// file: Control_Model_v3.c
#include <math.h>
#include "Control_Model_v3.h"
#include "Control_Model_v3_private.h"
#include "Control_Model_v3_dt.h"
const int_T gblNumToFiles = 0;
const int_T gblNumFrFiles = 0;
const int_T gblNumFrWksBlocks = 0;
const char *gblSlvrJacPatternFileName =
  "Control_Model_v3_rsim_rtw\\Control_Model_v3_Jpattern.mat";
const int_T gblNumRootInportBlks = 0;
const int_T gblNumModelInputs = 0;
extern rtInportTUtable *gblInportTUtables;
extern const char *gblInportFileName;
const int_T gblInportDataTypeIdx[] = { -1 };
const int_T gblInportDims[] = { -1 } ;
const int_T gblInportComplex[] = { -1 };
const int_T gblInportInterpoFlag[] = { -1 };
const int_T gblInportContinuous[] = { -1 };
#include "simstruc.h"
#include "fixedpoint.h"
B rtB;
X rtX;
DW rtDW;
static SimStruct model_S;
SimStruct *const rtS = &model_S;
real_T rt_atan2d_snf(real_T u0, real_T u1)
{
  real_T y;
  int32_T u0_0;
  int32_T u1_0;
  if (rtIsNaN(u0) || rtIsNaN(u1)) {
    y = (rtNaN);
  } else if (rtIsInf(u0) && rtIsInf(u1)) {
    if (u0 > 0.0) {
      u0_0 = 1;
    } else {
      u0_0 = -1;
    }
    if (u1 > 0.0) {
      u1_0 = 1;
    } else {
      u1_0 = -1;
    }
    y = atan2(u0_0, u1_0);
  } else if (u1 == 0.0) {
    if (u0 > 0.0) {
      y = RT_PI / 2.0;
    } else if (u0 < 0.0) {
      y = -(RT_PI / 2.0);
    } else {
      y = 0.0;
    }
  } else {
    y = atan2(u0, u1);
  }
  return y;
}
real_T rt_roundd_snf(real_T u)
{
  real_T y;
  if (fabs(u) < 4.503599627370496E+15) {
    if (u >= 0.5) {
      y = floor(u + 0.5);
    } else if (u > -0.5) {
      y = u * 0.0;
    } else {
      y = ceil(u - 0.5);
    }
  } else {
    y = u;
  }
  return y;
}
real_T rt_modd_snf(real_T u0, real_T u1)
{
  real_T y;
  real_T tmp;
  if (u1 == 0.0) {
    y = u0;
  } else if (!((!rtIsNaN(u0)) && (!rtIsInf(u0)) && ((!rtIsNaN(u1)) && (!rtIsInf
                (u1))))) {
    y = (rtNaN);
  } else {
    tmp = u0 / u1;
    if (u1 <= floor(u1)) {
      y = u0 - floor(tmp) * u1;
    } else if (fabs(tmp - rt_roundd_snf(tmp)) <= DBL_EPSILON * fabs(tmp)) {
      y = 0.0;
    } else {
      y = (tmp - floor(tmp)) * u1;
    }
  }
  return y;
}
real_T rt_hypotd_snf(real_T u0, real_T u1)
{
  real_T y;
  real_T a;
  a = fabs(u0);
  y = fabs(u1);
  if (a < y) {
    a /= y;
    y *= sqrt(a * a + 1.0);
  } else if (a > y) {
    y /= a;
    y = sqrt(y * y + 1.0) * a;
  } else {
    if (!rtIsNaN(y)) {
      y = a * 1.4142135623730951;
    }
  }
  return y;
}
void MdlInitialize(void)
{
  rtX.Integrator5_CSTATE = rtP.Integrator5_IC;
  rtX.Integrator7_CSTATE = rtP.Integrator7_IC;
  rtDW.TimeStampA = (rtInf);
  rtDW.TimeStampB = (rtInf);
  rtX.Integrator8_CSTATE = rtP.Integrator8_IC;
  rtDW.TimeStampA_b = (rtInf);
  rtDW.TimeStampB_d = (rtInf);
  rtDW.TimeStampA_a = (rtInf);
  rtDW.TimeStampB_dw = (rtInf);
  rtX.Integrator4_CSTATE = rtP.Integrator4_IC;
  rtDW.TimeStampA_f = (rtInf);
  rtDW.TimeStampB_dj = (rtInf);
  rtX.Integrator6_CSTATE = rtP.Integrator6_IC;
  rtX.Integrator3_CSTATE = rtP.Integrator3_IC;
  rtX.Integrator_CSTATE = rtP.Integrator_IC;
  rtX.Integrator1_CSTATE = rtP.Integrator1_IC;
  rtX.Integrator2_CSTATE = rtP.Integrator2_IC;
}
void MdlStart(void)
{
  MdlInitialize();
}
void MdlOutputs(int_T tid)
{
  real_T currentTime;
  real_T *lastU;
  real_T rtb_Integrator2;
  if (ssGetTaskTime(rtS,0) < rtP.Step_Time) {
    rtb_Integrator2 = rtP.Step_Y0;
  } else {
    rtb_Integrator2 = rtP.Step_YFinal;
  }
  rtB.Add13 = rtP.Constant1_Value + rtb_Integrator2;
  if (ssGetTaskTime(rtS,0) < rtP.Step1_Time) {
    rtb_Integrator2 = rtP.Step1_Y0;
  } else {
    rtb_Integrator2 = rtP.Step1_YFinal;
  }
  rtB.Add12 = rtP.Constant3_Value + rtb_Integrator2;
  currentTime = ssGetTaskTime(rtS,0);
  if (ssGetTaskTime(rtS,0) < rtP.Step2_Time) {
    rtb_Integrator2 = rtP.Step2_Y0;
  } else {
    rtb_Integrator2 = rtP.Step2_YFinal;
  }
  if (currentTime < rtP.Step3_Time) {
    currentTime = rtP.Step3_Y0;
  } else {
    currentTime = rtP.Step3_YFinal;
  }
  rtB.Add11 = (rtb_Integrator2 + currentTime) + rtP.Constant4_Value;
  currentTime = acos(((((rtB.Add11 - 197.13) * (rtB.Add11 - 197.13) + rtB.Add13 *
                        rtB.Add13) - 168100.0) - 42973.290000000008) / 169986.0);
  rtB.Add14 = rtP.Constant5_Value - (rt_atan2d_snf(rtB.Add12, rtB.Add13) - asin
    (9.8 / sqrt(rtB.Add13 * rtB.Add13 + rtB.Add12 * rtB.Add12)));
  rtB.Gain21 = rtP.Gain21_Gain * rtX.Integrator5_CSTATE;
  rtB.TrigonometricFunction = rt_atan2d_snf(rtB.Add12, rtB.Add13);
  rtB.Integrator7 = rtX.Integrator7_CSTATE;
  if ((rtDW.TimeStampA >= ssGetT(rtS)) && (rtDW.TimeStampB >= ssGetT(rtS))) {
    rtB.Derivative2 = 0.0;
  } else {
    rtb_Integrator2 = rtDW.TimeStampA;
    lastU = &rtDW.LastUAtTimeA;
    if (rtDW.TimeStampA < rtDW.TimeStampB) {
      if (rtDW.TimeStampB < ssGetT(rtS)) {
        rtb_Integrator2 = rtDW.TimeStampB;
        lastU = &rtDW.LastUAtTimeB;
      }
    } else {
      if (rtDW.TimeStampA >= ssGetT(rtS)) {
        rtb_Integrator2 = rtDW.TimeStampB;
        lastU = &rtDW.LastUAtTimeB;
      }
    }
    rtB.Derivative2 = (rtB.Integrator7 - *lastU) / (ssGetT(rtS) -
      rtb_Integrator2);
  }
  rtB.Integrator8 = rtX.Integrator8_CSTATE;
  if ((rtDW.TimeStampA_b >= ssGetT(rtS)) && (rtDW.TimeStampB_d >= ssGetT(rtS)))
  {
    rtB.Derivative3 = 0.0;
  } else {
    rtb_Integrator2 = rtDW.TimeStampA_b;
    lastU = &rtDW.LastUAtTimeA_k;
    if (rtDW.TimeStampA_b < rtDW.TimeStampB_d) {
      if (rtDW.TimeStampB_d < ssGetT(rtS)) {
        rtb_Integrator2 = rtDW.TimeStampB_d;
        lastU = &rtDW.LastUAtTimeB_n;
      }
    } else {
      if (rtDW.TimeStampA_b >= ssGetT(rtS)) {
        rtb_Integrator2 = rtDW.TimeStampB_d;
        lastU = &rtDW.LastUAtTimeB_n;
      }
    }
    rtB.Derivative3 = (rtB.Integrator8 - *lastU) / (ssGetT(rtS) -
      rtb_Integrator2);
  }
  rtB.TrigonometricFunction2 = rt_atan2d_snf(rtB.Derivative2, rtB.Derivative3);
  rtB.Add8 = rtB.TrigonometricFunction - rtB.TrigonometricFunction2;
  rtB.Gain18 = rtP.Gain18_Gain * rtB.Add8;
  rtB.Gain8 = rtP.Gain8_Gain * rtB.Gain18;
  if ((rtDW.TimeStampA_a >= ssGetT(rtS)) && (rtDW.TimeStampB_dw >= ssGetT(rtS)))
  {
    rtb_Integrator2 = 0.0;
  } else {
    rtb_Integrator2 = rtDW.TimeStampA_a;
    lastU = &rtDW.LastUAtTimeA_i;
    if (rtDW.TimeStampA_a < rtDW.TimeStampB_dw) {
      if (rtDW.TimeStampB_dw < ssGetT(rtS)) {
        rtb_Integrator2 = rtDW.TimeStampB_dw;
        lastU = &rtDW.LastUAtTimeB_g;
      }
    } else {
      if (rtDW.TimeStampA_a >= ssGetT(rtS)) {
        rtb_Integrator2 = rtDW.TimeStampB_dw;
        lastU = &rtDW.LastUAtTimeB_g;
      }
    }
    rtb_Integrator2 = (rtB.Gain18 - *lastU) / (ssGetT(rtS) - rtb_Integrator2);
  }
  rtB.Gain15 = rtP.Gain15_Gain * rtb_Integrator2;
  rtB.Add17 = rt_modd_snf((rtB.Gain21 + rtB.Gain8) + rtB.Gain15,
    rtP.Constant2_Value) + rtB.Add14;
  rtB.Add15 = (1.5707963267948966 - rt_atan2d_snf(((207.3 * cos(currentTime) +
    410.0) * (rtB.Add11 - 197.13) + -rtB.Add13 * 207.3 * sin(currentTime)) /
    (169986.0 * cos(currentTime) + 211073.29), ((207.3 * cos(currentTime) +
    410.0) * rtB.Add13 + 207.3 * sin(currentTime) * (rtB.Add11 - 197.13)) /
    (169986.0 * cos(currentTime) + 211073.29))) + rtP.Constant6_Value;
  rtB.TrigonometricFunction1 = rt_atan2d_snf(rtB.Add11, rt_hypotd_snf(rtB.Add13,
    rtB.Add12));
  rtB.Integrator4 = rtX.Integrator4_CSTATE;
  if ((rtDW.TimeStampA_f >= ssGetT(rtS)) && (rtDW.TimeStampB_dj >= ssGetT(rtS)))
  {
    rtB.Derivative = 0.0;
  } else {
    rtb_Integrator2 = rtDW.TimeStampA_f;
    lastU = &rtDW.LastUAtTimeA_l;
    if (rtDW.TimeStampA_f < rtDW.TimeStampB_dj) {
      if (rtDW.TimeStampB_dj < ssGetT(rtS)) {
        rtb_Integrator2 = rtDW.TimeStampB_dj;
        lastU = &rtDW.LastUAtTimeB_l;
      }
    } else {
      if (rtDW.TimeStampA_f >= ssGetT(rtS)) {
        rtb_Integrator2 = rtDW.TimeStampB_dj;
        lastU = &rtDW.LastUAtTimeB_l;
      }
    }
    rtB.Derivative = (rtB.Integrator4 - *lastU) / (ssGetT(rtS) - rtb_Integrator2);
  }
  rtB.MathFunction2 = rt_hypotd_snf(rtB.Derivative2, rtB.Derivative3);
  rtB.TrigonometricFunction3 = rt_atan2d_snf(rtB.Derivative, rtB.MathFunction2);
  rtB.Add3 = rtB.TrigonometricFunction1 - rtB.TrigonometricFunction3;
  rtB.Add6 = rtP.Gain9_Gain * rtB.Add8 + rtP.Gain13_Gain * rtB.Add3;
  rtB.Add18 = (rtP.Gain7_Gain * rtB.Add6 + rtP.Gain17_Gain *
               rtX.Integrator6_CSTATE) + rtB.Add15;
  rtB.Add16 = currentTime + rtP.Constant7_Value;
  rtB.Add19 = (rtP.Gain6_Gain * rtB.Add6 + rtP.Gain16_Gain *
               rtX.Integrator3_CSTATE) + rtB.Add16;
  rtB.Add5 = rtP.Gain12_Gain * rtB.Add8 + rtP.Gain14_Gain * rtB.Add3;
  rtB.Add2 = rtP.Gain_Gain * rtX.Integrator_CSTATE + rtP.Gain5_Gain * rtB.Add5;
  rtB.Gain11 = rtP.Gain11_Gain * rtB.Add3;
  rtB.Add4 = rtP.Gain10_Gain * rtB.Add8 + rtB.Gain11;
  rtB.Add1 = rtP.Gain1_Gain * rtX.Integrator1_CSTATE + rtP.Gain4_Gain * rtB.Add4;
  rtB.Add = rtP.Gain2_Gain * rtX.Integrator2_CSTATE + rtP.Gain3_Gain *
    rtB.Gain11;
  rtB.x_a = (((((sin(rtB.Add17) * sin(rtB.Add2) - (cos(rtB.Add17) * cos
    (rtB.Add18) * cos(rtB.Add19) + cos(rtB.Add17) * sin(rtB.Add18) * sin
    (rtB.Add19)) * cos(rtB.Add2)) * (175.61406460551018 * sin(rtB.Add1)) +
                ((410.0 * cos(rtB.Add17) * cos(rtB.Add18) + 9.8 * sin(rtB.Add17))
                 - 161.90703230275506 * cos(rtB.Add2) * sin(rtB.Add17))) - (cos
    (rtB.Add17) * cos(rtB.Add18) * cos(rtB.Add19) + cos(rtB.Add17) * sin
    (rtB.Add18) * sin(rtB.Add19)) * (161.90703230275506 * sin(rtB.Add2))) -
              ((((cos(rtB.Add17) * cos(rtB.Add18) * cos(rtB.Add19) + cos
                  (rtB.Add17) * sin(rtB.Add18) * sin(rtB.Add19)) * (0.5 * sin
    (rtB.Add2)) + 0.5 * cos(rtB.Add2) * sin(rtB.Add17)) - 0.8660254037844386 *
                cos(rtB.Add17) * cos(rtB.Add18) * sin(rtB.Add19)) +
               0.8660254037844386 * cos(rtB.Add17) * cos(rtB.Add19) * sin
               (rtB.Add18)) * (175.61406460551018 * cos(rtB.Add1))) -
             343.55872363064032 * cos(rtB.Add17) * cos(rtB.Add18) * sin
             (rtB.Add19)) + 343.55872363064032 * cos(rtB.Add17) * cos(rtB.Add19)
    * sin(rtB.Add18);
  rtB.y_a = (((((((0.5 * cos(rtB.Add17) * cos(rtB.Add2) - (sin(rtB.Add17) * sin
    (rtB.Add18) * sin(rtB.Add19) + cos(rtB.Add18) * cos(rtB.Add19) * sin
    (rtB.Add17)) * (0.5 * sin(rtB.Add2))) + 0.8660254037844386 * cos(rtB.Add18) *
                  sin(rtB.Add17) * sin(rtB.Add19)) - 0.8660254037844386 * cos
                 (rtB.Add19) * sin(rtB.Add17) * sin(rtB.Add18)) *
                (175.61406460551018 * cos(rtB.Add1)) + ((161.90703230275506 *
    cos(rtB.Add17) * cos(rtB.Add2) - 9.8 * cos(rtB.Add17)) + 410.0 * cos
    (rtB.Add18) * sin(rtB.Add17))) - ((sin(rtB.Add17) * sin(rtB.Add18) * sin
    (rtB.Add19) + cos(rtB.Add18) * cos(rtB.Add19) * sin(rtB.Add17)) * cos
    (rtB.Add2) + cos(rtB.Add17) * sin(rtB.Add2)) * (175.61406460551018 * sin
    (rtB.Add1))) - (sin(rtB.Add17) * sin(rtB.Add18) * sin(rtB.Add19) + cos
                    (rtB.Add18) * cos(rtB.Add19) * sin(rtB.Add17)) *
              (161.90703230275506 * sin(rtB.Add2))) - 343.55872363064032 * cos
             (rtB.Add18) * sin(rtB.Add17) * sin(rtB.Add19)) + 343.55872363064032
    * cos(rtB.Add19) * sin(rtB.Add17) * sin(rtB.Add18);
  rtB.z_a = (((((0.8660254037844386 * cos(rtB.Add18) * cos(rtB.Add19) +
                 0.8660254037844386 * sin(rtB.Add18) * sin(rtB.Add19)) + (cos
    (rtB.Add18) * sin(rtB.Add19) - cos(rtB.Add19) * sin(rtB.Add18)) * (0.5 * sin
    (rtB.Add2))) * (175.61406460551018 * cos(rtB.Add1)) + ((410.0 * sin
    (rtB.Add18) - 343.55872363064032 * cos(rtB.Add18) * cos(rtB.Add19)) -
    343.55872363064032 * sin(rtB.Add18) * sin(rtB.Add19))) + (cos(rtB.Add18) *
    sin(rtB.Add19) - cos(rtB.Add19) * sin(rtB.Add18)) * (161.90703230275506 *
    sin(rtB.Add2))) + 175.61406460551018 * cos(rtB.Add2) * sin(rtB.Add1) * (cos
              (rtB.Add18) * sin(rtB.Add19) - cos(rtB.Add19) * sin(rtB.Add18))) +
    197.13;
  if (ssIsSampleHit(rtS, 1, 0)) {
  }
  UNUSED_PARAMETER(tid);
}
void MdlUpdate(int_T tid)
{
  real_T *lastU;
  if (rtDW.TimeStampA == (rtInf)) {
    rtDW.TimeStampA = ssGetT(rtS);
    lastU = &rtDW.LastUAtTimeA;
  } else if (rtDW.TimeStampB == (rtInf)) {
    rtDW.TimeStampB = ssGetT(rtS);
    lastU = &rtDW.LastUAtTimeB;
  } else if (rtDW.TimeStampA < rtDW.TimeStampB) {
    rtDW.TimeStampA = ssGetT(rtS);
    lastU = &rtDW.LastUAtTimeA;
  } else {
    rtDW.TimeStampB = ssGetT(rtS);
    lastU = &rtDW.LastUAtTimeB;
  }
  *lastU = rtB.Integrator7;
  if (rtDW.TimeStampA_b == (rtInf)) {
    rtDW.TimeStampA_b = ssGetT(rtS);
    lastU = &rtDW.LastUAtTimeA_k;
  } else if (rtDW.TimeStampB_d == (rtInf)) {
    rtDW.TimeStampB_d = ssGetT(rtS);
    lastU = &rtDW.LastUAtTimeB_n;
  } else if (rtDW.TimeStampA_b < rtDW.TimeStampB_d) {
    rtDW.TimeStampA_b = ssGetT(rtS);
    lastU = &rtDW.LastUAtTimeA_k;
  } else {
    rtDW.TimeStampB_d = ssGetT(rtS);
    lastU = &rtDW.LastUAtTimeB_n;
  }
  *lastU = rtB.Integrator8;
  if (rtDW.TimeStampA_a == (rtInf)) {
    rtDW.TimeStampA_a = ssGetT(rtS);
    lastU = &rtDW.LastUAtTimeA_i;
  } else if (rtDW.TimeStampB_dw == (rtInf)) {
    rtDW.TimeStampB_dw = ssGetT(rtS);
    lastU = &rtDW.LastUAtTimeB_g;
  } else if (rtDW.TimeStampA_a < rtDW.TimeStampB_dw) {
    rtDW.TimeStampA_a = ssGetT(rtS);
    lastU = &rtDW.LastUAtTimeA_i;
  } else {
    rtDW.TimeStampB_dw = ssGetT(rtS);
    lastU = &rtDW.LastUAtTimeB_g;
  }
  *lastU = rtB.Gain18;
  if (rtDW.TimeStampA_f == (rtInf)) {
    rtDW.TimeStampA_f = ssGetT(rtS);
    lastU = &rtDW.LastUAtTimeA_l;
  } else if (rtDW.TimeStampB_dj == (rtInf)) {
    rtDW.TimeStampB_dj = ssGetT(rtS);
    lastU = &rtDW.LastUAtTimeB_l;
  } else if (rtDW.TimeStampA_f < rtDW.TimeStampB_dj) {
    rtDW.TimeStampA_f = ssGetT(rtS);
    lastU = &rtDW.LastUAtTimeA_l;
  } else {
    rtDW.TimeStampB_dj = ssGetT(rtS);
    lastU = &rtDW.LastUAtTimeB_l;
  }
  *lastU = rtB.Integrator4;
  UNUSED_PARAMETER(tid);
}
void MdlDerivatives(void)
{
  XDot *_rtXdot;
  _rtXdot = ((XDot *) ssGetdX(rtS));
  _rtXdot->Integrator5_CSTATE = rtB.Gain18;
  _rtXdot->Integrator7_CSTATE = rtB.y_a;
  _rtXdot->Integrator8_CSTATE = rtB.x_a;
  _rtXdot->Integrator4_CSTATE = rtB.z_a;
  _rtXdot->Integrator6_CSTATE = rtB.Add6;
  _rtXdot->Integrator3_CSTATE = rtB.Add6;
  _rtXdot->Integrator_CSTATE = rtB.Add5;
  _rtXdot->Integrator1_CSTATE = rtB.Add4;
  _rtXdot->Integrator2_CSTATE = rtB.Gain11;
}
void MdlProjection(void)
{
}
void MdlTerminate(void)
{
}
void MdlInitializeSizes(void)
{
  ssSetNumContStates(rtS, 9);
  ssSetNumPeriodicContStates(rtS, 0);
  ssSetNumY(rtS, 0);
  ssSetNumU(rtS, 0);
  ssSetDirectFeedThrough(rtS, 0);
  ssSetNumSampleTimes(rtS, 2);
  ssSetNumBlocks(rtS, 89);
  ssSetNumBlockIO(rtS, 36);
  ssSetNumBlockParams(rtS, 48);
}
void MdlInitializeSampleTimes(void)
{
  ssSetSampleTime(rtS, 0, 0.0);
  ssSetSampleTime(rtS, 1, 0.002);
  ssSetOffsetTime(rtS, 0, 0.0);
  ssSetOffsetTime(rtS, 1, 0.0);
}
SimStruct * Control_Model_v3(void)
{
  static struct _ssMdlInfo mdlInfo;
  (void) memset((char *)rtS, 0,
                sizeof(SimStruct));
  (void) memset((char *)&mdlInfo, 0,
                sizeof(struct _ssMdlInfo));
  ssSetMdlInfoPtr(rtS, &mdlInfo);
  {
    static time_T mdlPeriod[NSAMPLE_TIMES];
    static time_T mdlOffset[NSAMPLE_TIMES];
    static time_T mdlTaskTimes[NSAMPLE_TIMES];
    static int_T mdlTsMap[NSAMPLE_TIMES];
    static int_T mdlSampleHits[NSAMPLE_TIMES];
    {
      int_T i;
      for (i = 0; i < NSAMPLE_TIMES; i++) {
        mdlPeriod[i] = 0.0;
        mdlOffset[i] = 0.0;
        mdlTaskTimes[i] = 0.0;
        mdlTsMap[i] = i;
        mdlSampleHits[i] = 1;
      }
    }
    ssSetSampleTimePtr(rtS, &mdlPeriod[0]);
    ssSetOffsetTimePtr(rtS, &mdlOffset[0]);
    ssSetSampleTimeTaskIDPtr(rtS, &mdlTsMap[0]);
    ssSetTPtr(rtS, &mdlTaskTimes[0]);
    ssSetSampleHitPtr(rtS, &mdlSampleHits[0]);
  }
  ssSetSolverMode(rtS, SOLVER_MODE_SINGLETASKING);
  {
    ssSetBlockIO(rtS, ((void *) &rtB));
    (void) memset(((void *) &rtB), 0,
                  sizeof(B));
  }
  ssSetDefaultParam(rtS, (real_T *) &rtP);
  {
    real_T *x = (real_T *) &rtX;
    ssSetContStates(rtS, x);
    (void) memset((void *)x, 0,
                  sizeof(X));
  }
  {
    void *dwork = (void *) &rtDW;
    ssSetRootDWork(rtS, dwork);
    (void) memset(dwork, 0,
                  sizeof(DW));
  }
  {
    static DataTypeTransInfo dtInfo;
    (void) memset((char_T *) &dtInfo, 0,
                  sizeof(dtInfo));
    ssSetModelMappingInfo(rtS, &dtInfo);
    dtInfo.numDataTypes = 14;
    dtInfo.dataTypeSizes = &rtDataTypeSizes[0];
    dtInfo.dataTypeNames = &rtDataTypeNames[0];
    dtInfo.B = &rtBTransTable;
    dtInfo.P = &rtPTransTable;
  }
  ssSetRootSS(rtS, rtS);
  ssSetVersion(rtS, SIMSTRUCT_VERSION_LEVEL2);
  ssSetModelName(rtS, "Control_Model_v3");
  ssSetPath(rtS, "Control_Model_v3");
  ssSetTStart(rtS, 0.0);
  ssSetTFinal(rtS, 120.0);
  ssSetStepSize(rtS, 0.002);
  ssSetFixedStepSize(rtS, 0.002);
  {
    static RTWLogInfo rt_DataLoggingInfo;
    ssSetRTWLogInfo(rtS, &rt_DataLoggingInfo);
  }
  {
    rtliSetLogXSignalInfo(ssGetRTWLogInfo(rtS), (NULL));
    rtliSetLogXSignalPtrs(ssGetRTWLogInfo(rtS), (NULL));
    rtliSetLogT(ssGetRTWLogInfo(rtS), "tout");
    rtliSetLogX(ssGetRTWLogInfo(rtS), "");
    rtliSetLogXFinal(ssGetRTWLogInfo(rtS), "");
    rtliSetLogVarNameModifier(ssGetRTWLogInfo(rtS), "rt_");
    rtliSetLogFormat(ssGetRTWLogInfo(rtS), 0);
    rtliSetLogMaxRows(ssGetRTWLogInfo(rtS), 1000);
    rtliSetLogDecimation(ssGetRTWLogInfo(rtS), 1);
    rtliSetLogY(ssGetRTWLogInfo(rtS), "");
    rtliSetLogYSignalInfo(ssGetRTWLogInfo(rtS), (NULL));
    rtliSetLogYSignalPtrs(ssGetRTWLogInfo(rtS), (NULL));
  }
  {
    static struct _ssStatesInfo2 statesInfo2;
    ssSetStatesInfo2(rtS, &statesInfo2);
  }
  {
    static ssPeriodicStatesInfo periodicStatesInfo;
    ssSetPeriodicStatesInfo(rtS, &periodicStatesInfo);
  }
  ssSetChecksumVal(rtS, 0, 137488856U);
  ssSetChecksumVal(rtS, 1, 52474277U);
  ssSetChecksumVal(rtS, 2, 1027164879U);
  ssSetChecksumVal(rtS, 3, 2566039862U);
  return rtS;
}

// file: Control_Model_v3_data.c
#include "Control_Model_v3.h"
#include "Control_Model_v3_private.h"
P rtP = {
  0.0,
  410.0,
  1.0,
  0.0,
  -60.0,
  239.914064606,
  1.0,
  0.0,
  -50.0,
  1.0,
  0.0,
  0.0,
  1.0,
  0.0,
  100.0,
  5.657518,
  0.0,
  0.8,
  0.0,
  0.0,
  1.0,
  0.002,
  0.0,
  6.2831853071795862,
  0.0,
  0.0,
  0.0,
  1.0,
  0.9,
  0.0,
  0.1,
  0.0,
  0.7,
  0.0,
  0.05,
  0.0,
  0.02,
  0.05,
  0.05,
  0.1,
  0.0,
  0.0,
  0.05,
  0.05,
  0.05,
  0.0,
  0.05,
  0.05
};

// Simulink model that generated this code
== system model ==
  Integrator5 : Integrator  <- 1: Gain18
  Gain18 : Gain  <- 1: Add8
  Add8 : Sum  Inputs=+-  <- 1: TrigonometricFunction, 2: TrigonometricFunction2
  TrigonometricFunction : Trigonometry  Operator=atan2  <- 1: Add12, 2: Add13
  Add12 : Sum  Inputs=+++  <- 1: Constant3, 2: Step1
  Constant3 : Constant  Value=239.914064606
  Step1 : Step  After=-50
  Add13 : Sum  Inputs=+++  <- 1: Constant1, 2: Step
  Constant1 : Constant  Value=410
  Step : Step  After=-60
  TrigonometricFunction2 : Trigonometry  Operator=atan2  <- 1: Derivative2, 2: Derivative3
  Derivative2 : Derivative  <- 1: Integrator7
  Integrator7 : Integrator  <- 1: MATLABFunction#1/2
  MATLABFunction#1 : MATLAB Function  <- 1: Add17, 2: Add18, 3: Add19, 4: Add2, 5: Add1, 6: Add
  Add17 : Sum  <- 1: Add14, 2: Math#1
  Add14 : Sum  Inputs=+-  <- 1: Constant5, 2: MATLABFunction#2
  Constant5 : Constant  Value=0
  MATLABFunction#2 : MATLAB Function  <- 1: Add13, 2: Add12, 3: Add11
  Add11 : Sum  Inputs=+++  <- 1: Step2, 2: Step3, 3: Constant4
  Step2 : Step  After=0
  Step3 : Step  After=100
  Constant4 : Constant  Value=5.657518
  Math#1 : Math  Operator=mod  <- 1: Sum#1, 2: Constant2
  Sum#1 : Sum  Inputs=+++  <- 1: Gain21, 2: Gain8, 3: Gain15
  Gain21 : Gain  Gain=0.8  <- 1: Integrator5
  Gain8 : Gain  Gain=0.002  <- 1: Gain18
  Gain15 : Gain  Gain=0  <- 1: Derivative#1
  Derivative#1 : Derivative  <- 1: Gain18
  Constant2 : Constant  Value=2*pi
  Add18 : Sum  <- 1: Add15, 2: Sum#2
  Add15 : Sum  <- 1: Constant6, 2: MATLABFunction#2/2
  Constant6 : Constant  Value=0
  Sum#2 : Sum  <- 1: Gain7, 2: Gain17
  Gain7 : Gain  Gain=0.9  <- 1: Add6
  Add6 : Sum  <- 1: Gain9, 2: Gain13
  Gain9 : Gain  Gain=0  <- 1: Add8
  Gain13 : Gain  <- 1: Add3
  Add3 : Sum  Inputs=+-  <- 1: TrigonometricFunction1, 2: TrigonometricFunction3
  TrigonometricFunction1 : Trigonometry  Operator=atan2  <- 1: Add11, 2: Math#2
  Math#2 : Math  Operator=hypot  <- 1: Add13, 2: Add12
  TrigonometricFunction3 : Trigonometry  Operator=atan2  <- 1: Derivative, 2: MathFunction2
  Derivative : Derivative  <- 1: Integrator4
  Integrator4 : Integrator  <- 1: MATLABFunction#1/3
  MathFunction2 : Math  Operator=hypot  <- 1: Derivative2, 2: Derivative3
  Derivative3 : Derivative  <- 1: Integrator8
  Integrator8 : Integrator  <- 1: MATLABFunction#1
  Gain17 : Gain  Gain=0.1  <- 1: Integrator6
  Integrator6 : Integrator  <- 1: Add6
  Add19 : Sum  <- 1: Add16, 2: Sum#3
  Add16 : Sum  <- 1: MATLABFunction#2/3, 2: Constant7
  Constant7 : Constant  Value=0
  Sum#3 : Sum  <- 1: Gain6, 2: Gain16
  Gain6 : Gain  Gain=0.7  <- 1: Add6
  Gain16 : Gain  Gain=0.05  <- 1: Integrator3
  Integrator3 : Integrator  <- 1: Add6
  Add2 : Sum  <- 1: Gain, 2: Gain5
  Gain : Gain  Gain=0.02  <- 1: Integrator
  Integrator : Integrator  <- 1: Add5
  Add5 : Sum  <- 1: Gain12, 2: Gain14
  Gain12 : Gain  Gain=0.05  <- 1: Add8
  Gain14 : Gain  Gain=0.05  <- 1: Add3
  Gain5 : Gain  Gain=0.1  <- 1: Add5
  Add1 : Sum  <- 1: Gain1, 2: Gain4
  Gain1 : Gain  Gain=0  <- 1: Integrator1
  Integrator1 : Integrator  <- 1: Add4
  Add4 : Sum  <- 1: Gain10, 2: Gain11
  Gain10 : Gain  Gain=0.05  <- 1: Add8
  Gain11 : Gain  Gain=0.05  <- 1: Add3
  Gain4 : Gain  Gain=0.05  <- 1: Add4
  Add : Sum  <- 1: Gain2, 2: Gain3
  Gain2 : Gain  Gain=0.05  <- 1: Integrator2
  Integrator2 : Integrator  <- 1: Gain11
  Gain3 : Gain  Gain=0.05  <- 1: Gain11
== matlab function MATLABFunction#2 ==
function [q_1, q_2, q_3] = fcn( px, py, pz)
%#codegen

D1 = 197.13;%275.5;
D2 = 410;
D3 = 207.3;
D4 = 74.1;
D5 = 74.1;
D6 = 160.0;
e2 = 9.8;
d1 = 197.13;
d2 = D2;
d3 = D3;

% q_3 +
%q_3__ = 1 * acos( (px^2 + (pz-d1)^2 - d2^2 - d3^2) / (2*d2*d3) );  

%cq_2 = (px*(d2+d3*cos(q_3__)) + d3*sin(q_3__)*(pz -d1)) / (d2^2 + d3^2 + 2*d2*d3*cos(q_3__));
%sq_2 = (-px*d3*sin(q_3__) + (d2+d3*cos(q_3__))*(pz -d1)) / (d2^2 + d3^2 + 2*d2*d3*cos(q_3__));
%q_2__ = (pi/2) - atan2(sq_2,cq_2);
%q_3__*180/pi
%q_2__*180/pi
% q_3 -

q_3 = 1 * acos( (px^2 + (pz-d1)^2 - d2^2 - d3^2) / (2*d2*d3) );  

cq_2 = (px*(d2+d3*cos(q_3)) + d3*sin(q_3)*(pz -d1)) / (d2^2 + d3^2 + 2*d2*d3*cos(q_3));
sq_2 = (-px*d3*sin(q_3) + (d2+d3*cos(q_3))*(pz -d1)) / (d2^2 + d3^2 + 2*d2*d3*cos(q_3));
q_2 = (pi/2) - atan2(sq_2,cq_2);

% q_1 offset
q_1 = atan2((py), px) - asin(e2 / ((px^2 + py^2)^.5));

== matlab function MATLABFunction#1 ==
function [x_a, y_a, z_a] = fcn(q_1, q_2, q_3, q_4, q_5, q_6)
%#codegen

q1 = q_1;%pi-(q_1);
q2 = q_2;%-pi/2 + (q_2+pi);
q3 = q_3;%pi/2 + (pi+q_3);
q4 = q_4;%q_4;
q5 = q_5;%-pi + q_5;
q6 = q_6;%pi + q_6;

%A_new = vpa(subs(A, [q1,q2,q3,q4,q5,q6], [ pi-(q_1), -pi/2 + (q_2+pi), pi/2 + (pi+q_3), q_4, -pi + q_5, pi]));

x_a = 9.8*sin(q1) + 410.0*cos(q1)*cos(q2) - 161.90703230275506147226218323136*cos(q4)*sin(q1) + 175.614064605510166451876962007*sin(q5)*(1.0*sin(q1)*sin(q4) - cos(q4)*(cos(q1)*cos(q2)*cos(q3) + cos(q1)*sin(q2)*sin(q3))) - 161.90703230275506147226218323136*sin(q4)*(cos(q1)*cos(q2)*cos(q3) + cos(q1)*sin(q2)*sin(q3)) - 175.614064605510166451876962007*cos(q5)*(0.5*cos(q4)*sin(q1) + 0.5*sin(q4)*(cos(q1)*cos(q2)*cos(q3) + cos(q1)*sin(q2)*sin(q3)) - 0.86602540378443864676372317075294*cos(q1)*cos(q2)*sin(q3) + 0.86602540378443864676372317075294*cos(q1)*cos(q3)*sin(q2)) - 343.55872363064032981583295622841*cos(q1)*cos(q2)*sin(q3) + 343.55872363064032981583295622841*cos(q1)*cos(q3)*sin(q2); 
y_a = 161.90703230275506147226218323136*cos(q1)*cos(q4) - 9.8*cos(q1) + 410.0*cos(q2)*sin(q1) + 175.614064605510166451876962007*cos(q5)*(0.5*cos(q1)*cos(q4) - 0.5*sin(q4)*(sin(q1)*sin(q2)*sin(q3) + cos(q2)*cos(q3)*sin(q1)) + 0.86602540378443864676372317075294*cos(q2)*sin(q1)*sin(q3) - 0.86602540378443864676372317075294*cos(q3)*sin(q1)*sin(q2)) - 175.614064605510166451876962007*sin(q5)*(1.0*cos(q1)*sin(q4) + cos(q4)*(sin(q1)*sin(q2)*sin(q3) + cos(q2)*cos(q3)*sin(q1))) - 161.90703230275506147226218323136*sin(q4)*(sin(q1)*sin(q2)*sin(q3) + cos(q2)*cos(q3)*sin(q1)) - 343.55872363064032981583295622841*cos(q2)*sin(q1)*sin(q3) + 343.55872363064032981583295622841*cos(q3)*sin(q1)*sin(q2);
z_a = 410.0*sin(q2) - 343.55872363064032981583295622841*cos(q2)*cos(q3) - 343.55872363064032981583295622841*sin(q2)*sin(q3) + 175.614064605510166451876962007*cos(q5)*(0.86602540378443864676372317075294*cos(q2)*cos(q3) + 0.86602540378443864676372317075294*sin(q2)*sin(q3) + 0.5*sin(q4)*(1.0*cos(q2)*sin(q3) - 1.0*cos(q3)*sin(q2))) + 161.90703230275506147226218323136*sin(q4)*(1.0*cos(q2)*sin(q3) - 1.0*cos(q3)*sin(q2)) + 175.614064605510166451876962007*cos(q4)*sin(q5)*(1.0*cos(q2)*sin(q3) - 1.0*cos(q3)*sin(q2)) + 197.13;

%y = u;
